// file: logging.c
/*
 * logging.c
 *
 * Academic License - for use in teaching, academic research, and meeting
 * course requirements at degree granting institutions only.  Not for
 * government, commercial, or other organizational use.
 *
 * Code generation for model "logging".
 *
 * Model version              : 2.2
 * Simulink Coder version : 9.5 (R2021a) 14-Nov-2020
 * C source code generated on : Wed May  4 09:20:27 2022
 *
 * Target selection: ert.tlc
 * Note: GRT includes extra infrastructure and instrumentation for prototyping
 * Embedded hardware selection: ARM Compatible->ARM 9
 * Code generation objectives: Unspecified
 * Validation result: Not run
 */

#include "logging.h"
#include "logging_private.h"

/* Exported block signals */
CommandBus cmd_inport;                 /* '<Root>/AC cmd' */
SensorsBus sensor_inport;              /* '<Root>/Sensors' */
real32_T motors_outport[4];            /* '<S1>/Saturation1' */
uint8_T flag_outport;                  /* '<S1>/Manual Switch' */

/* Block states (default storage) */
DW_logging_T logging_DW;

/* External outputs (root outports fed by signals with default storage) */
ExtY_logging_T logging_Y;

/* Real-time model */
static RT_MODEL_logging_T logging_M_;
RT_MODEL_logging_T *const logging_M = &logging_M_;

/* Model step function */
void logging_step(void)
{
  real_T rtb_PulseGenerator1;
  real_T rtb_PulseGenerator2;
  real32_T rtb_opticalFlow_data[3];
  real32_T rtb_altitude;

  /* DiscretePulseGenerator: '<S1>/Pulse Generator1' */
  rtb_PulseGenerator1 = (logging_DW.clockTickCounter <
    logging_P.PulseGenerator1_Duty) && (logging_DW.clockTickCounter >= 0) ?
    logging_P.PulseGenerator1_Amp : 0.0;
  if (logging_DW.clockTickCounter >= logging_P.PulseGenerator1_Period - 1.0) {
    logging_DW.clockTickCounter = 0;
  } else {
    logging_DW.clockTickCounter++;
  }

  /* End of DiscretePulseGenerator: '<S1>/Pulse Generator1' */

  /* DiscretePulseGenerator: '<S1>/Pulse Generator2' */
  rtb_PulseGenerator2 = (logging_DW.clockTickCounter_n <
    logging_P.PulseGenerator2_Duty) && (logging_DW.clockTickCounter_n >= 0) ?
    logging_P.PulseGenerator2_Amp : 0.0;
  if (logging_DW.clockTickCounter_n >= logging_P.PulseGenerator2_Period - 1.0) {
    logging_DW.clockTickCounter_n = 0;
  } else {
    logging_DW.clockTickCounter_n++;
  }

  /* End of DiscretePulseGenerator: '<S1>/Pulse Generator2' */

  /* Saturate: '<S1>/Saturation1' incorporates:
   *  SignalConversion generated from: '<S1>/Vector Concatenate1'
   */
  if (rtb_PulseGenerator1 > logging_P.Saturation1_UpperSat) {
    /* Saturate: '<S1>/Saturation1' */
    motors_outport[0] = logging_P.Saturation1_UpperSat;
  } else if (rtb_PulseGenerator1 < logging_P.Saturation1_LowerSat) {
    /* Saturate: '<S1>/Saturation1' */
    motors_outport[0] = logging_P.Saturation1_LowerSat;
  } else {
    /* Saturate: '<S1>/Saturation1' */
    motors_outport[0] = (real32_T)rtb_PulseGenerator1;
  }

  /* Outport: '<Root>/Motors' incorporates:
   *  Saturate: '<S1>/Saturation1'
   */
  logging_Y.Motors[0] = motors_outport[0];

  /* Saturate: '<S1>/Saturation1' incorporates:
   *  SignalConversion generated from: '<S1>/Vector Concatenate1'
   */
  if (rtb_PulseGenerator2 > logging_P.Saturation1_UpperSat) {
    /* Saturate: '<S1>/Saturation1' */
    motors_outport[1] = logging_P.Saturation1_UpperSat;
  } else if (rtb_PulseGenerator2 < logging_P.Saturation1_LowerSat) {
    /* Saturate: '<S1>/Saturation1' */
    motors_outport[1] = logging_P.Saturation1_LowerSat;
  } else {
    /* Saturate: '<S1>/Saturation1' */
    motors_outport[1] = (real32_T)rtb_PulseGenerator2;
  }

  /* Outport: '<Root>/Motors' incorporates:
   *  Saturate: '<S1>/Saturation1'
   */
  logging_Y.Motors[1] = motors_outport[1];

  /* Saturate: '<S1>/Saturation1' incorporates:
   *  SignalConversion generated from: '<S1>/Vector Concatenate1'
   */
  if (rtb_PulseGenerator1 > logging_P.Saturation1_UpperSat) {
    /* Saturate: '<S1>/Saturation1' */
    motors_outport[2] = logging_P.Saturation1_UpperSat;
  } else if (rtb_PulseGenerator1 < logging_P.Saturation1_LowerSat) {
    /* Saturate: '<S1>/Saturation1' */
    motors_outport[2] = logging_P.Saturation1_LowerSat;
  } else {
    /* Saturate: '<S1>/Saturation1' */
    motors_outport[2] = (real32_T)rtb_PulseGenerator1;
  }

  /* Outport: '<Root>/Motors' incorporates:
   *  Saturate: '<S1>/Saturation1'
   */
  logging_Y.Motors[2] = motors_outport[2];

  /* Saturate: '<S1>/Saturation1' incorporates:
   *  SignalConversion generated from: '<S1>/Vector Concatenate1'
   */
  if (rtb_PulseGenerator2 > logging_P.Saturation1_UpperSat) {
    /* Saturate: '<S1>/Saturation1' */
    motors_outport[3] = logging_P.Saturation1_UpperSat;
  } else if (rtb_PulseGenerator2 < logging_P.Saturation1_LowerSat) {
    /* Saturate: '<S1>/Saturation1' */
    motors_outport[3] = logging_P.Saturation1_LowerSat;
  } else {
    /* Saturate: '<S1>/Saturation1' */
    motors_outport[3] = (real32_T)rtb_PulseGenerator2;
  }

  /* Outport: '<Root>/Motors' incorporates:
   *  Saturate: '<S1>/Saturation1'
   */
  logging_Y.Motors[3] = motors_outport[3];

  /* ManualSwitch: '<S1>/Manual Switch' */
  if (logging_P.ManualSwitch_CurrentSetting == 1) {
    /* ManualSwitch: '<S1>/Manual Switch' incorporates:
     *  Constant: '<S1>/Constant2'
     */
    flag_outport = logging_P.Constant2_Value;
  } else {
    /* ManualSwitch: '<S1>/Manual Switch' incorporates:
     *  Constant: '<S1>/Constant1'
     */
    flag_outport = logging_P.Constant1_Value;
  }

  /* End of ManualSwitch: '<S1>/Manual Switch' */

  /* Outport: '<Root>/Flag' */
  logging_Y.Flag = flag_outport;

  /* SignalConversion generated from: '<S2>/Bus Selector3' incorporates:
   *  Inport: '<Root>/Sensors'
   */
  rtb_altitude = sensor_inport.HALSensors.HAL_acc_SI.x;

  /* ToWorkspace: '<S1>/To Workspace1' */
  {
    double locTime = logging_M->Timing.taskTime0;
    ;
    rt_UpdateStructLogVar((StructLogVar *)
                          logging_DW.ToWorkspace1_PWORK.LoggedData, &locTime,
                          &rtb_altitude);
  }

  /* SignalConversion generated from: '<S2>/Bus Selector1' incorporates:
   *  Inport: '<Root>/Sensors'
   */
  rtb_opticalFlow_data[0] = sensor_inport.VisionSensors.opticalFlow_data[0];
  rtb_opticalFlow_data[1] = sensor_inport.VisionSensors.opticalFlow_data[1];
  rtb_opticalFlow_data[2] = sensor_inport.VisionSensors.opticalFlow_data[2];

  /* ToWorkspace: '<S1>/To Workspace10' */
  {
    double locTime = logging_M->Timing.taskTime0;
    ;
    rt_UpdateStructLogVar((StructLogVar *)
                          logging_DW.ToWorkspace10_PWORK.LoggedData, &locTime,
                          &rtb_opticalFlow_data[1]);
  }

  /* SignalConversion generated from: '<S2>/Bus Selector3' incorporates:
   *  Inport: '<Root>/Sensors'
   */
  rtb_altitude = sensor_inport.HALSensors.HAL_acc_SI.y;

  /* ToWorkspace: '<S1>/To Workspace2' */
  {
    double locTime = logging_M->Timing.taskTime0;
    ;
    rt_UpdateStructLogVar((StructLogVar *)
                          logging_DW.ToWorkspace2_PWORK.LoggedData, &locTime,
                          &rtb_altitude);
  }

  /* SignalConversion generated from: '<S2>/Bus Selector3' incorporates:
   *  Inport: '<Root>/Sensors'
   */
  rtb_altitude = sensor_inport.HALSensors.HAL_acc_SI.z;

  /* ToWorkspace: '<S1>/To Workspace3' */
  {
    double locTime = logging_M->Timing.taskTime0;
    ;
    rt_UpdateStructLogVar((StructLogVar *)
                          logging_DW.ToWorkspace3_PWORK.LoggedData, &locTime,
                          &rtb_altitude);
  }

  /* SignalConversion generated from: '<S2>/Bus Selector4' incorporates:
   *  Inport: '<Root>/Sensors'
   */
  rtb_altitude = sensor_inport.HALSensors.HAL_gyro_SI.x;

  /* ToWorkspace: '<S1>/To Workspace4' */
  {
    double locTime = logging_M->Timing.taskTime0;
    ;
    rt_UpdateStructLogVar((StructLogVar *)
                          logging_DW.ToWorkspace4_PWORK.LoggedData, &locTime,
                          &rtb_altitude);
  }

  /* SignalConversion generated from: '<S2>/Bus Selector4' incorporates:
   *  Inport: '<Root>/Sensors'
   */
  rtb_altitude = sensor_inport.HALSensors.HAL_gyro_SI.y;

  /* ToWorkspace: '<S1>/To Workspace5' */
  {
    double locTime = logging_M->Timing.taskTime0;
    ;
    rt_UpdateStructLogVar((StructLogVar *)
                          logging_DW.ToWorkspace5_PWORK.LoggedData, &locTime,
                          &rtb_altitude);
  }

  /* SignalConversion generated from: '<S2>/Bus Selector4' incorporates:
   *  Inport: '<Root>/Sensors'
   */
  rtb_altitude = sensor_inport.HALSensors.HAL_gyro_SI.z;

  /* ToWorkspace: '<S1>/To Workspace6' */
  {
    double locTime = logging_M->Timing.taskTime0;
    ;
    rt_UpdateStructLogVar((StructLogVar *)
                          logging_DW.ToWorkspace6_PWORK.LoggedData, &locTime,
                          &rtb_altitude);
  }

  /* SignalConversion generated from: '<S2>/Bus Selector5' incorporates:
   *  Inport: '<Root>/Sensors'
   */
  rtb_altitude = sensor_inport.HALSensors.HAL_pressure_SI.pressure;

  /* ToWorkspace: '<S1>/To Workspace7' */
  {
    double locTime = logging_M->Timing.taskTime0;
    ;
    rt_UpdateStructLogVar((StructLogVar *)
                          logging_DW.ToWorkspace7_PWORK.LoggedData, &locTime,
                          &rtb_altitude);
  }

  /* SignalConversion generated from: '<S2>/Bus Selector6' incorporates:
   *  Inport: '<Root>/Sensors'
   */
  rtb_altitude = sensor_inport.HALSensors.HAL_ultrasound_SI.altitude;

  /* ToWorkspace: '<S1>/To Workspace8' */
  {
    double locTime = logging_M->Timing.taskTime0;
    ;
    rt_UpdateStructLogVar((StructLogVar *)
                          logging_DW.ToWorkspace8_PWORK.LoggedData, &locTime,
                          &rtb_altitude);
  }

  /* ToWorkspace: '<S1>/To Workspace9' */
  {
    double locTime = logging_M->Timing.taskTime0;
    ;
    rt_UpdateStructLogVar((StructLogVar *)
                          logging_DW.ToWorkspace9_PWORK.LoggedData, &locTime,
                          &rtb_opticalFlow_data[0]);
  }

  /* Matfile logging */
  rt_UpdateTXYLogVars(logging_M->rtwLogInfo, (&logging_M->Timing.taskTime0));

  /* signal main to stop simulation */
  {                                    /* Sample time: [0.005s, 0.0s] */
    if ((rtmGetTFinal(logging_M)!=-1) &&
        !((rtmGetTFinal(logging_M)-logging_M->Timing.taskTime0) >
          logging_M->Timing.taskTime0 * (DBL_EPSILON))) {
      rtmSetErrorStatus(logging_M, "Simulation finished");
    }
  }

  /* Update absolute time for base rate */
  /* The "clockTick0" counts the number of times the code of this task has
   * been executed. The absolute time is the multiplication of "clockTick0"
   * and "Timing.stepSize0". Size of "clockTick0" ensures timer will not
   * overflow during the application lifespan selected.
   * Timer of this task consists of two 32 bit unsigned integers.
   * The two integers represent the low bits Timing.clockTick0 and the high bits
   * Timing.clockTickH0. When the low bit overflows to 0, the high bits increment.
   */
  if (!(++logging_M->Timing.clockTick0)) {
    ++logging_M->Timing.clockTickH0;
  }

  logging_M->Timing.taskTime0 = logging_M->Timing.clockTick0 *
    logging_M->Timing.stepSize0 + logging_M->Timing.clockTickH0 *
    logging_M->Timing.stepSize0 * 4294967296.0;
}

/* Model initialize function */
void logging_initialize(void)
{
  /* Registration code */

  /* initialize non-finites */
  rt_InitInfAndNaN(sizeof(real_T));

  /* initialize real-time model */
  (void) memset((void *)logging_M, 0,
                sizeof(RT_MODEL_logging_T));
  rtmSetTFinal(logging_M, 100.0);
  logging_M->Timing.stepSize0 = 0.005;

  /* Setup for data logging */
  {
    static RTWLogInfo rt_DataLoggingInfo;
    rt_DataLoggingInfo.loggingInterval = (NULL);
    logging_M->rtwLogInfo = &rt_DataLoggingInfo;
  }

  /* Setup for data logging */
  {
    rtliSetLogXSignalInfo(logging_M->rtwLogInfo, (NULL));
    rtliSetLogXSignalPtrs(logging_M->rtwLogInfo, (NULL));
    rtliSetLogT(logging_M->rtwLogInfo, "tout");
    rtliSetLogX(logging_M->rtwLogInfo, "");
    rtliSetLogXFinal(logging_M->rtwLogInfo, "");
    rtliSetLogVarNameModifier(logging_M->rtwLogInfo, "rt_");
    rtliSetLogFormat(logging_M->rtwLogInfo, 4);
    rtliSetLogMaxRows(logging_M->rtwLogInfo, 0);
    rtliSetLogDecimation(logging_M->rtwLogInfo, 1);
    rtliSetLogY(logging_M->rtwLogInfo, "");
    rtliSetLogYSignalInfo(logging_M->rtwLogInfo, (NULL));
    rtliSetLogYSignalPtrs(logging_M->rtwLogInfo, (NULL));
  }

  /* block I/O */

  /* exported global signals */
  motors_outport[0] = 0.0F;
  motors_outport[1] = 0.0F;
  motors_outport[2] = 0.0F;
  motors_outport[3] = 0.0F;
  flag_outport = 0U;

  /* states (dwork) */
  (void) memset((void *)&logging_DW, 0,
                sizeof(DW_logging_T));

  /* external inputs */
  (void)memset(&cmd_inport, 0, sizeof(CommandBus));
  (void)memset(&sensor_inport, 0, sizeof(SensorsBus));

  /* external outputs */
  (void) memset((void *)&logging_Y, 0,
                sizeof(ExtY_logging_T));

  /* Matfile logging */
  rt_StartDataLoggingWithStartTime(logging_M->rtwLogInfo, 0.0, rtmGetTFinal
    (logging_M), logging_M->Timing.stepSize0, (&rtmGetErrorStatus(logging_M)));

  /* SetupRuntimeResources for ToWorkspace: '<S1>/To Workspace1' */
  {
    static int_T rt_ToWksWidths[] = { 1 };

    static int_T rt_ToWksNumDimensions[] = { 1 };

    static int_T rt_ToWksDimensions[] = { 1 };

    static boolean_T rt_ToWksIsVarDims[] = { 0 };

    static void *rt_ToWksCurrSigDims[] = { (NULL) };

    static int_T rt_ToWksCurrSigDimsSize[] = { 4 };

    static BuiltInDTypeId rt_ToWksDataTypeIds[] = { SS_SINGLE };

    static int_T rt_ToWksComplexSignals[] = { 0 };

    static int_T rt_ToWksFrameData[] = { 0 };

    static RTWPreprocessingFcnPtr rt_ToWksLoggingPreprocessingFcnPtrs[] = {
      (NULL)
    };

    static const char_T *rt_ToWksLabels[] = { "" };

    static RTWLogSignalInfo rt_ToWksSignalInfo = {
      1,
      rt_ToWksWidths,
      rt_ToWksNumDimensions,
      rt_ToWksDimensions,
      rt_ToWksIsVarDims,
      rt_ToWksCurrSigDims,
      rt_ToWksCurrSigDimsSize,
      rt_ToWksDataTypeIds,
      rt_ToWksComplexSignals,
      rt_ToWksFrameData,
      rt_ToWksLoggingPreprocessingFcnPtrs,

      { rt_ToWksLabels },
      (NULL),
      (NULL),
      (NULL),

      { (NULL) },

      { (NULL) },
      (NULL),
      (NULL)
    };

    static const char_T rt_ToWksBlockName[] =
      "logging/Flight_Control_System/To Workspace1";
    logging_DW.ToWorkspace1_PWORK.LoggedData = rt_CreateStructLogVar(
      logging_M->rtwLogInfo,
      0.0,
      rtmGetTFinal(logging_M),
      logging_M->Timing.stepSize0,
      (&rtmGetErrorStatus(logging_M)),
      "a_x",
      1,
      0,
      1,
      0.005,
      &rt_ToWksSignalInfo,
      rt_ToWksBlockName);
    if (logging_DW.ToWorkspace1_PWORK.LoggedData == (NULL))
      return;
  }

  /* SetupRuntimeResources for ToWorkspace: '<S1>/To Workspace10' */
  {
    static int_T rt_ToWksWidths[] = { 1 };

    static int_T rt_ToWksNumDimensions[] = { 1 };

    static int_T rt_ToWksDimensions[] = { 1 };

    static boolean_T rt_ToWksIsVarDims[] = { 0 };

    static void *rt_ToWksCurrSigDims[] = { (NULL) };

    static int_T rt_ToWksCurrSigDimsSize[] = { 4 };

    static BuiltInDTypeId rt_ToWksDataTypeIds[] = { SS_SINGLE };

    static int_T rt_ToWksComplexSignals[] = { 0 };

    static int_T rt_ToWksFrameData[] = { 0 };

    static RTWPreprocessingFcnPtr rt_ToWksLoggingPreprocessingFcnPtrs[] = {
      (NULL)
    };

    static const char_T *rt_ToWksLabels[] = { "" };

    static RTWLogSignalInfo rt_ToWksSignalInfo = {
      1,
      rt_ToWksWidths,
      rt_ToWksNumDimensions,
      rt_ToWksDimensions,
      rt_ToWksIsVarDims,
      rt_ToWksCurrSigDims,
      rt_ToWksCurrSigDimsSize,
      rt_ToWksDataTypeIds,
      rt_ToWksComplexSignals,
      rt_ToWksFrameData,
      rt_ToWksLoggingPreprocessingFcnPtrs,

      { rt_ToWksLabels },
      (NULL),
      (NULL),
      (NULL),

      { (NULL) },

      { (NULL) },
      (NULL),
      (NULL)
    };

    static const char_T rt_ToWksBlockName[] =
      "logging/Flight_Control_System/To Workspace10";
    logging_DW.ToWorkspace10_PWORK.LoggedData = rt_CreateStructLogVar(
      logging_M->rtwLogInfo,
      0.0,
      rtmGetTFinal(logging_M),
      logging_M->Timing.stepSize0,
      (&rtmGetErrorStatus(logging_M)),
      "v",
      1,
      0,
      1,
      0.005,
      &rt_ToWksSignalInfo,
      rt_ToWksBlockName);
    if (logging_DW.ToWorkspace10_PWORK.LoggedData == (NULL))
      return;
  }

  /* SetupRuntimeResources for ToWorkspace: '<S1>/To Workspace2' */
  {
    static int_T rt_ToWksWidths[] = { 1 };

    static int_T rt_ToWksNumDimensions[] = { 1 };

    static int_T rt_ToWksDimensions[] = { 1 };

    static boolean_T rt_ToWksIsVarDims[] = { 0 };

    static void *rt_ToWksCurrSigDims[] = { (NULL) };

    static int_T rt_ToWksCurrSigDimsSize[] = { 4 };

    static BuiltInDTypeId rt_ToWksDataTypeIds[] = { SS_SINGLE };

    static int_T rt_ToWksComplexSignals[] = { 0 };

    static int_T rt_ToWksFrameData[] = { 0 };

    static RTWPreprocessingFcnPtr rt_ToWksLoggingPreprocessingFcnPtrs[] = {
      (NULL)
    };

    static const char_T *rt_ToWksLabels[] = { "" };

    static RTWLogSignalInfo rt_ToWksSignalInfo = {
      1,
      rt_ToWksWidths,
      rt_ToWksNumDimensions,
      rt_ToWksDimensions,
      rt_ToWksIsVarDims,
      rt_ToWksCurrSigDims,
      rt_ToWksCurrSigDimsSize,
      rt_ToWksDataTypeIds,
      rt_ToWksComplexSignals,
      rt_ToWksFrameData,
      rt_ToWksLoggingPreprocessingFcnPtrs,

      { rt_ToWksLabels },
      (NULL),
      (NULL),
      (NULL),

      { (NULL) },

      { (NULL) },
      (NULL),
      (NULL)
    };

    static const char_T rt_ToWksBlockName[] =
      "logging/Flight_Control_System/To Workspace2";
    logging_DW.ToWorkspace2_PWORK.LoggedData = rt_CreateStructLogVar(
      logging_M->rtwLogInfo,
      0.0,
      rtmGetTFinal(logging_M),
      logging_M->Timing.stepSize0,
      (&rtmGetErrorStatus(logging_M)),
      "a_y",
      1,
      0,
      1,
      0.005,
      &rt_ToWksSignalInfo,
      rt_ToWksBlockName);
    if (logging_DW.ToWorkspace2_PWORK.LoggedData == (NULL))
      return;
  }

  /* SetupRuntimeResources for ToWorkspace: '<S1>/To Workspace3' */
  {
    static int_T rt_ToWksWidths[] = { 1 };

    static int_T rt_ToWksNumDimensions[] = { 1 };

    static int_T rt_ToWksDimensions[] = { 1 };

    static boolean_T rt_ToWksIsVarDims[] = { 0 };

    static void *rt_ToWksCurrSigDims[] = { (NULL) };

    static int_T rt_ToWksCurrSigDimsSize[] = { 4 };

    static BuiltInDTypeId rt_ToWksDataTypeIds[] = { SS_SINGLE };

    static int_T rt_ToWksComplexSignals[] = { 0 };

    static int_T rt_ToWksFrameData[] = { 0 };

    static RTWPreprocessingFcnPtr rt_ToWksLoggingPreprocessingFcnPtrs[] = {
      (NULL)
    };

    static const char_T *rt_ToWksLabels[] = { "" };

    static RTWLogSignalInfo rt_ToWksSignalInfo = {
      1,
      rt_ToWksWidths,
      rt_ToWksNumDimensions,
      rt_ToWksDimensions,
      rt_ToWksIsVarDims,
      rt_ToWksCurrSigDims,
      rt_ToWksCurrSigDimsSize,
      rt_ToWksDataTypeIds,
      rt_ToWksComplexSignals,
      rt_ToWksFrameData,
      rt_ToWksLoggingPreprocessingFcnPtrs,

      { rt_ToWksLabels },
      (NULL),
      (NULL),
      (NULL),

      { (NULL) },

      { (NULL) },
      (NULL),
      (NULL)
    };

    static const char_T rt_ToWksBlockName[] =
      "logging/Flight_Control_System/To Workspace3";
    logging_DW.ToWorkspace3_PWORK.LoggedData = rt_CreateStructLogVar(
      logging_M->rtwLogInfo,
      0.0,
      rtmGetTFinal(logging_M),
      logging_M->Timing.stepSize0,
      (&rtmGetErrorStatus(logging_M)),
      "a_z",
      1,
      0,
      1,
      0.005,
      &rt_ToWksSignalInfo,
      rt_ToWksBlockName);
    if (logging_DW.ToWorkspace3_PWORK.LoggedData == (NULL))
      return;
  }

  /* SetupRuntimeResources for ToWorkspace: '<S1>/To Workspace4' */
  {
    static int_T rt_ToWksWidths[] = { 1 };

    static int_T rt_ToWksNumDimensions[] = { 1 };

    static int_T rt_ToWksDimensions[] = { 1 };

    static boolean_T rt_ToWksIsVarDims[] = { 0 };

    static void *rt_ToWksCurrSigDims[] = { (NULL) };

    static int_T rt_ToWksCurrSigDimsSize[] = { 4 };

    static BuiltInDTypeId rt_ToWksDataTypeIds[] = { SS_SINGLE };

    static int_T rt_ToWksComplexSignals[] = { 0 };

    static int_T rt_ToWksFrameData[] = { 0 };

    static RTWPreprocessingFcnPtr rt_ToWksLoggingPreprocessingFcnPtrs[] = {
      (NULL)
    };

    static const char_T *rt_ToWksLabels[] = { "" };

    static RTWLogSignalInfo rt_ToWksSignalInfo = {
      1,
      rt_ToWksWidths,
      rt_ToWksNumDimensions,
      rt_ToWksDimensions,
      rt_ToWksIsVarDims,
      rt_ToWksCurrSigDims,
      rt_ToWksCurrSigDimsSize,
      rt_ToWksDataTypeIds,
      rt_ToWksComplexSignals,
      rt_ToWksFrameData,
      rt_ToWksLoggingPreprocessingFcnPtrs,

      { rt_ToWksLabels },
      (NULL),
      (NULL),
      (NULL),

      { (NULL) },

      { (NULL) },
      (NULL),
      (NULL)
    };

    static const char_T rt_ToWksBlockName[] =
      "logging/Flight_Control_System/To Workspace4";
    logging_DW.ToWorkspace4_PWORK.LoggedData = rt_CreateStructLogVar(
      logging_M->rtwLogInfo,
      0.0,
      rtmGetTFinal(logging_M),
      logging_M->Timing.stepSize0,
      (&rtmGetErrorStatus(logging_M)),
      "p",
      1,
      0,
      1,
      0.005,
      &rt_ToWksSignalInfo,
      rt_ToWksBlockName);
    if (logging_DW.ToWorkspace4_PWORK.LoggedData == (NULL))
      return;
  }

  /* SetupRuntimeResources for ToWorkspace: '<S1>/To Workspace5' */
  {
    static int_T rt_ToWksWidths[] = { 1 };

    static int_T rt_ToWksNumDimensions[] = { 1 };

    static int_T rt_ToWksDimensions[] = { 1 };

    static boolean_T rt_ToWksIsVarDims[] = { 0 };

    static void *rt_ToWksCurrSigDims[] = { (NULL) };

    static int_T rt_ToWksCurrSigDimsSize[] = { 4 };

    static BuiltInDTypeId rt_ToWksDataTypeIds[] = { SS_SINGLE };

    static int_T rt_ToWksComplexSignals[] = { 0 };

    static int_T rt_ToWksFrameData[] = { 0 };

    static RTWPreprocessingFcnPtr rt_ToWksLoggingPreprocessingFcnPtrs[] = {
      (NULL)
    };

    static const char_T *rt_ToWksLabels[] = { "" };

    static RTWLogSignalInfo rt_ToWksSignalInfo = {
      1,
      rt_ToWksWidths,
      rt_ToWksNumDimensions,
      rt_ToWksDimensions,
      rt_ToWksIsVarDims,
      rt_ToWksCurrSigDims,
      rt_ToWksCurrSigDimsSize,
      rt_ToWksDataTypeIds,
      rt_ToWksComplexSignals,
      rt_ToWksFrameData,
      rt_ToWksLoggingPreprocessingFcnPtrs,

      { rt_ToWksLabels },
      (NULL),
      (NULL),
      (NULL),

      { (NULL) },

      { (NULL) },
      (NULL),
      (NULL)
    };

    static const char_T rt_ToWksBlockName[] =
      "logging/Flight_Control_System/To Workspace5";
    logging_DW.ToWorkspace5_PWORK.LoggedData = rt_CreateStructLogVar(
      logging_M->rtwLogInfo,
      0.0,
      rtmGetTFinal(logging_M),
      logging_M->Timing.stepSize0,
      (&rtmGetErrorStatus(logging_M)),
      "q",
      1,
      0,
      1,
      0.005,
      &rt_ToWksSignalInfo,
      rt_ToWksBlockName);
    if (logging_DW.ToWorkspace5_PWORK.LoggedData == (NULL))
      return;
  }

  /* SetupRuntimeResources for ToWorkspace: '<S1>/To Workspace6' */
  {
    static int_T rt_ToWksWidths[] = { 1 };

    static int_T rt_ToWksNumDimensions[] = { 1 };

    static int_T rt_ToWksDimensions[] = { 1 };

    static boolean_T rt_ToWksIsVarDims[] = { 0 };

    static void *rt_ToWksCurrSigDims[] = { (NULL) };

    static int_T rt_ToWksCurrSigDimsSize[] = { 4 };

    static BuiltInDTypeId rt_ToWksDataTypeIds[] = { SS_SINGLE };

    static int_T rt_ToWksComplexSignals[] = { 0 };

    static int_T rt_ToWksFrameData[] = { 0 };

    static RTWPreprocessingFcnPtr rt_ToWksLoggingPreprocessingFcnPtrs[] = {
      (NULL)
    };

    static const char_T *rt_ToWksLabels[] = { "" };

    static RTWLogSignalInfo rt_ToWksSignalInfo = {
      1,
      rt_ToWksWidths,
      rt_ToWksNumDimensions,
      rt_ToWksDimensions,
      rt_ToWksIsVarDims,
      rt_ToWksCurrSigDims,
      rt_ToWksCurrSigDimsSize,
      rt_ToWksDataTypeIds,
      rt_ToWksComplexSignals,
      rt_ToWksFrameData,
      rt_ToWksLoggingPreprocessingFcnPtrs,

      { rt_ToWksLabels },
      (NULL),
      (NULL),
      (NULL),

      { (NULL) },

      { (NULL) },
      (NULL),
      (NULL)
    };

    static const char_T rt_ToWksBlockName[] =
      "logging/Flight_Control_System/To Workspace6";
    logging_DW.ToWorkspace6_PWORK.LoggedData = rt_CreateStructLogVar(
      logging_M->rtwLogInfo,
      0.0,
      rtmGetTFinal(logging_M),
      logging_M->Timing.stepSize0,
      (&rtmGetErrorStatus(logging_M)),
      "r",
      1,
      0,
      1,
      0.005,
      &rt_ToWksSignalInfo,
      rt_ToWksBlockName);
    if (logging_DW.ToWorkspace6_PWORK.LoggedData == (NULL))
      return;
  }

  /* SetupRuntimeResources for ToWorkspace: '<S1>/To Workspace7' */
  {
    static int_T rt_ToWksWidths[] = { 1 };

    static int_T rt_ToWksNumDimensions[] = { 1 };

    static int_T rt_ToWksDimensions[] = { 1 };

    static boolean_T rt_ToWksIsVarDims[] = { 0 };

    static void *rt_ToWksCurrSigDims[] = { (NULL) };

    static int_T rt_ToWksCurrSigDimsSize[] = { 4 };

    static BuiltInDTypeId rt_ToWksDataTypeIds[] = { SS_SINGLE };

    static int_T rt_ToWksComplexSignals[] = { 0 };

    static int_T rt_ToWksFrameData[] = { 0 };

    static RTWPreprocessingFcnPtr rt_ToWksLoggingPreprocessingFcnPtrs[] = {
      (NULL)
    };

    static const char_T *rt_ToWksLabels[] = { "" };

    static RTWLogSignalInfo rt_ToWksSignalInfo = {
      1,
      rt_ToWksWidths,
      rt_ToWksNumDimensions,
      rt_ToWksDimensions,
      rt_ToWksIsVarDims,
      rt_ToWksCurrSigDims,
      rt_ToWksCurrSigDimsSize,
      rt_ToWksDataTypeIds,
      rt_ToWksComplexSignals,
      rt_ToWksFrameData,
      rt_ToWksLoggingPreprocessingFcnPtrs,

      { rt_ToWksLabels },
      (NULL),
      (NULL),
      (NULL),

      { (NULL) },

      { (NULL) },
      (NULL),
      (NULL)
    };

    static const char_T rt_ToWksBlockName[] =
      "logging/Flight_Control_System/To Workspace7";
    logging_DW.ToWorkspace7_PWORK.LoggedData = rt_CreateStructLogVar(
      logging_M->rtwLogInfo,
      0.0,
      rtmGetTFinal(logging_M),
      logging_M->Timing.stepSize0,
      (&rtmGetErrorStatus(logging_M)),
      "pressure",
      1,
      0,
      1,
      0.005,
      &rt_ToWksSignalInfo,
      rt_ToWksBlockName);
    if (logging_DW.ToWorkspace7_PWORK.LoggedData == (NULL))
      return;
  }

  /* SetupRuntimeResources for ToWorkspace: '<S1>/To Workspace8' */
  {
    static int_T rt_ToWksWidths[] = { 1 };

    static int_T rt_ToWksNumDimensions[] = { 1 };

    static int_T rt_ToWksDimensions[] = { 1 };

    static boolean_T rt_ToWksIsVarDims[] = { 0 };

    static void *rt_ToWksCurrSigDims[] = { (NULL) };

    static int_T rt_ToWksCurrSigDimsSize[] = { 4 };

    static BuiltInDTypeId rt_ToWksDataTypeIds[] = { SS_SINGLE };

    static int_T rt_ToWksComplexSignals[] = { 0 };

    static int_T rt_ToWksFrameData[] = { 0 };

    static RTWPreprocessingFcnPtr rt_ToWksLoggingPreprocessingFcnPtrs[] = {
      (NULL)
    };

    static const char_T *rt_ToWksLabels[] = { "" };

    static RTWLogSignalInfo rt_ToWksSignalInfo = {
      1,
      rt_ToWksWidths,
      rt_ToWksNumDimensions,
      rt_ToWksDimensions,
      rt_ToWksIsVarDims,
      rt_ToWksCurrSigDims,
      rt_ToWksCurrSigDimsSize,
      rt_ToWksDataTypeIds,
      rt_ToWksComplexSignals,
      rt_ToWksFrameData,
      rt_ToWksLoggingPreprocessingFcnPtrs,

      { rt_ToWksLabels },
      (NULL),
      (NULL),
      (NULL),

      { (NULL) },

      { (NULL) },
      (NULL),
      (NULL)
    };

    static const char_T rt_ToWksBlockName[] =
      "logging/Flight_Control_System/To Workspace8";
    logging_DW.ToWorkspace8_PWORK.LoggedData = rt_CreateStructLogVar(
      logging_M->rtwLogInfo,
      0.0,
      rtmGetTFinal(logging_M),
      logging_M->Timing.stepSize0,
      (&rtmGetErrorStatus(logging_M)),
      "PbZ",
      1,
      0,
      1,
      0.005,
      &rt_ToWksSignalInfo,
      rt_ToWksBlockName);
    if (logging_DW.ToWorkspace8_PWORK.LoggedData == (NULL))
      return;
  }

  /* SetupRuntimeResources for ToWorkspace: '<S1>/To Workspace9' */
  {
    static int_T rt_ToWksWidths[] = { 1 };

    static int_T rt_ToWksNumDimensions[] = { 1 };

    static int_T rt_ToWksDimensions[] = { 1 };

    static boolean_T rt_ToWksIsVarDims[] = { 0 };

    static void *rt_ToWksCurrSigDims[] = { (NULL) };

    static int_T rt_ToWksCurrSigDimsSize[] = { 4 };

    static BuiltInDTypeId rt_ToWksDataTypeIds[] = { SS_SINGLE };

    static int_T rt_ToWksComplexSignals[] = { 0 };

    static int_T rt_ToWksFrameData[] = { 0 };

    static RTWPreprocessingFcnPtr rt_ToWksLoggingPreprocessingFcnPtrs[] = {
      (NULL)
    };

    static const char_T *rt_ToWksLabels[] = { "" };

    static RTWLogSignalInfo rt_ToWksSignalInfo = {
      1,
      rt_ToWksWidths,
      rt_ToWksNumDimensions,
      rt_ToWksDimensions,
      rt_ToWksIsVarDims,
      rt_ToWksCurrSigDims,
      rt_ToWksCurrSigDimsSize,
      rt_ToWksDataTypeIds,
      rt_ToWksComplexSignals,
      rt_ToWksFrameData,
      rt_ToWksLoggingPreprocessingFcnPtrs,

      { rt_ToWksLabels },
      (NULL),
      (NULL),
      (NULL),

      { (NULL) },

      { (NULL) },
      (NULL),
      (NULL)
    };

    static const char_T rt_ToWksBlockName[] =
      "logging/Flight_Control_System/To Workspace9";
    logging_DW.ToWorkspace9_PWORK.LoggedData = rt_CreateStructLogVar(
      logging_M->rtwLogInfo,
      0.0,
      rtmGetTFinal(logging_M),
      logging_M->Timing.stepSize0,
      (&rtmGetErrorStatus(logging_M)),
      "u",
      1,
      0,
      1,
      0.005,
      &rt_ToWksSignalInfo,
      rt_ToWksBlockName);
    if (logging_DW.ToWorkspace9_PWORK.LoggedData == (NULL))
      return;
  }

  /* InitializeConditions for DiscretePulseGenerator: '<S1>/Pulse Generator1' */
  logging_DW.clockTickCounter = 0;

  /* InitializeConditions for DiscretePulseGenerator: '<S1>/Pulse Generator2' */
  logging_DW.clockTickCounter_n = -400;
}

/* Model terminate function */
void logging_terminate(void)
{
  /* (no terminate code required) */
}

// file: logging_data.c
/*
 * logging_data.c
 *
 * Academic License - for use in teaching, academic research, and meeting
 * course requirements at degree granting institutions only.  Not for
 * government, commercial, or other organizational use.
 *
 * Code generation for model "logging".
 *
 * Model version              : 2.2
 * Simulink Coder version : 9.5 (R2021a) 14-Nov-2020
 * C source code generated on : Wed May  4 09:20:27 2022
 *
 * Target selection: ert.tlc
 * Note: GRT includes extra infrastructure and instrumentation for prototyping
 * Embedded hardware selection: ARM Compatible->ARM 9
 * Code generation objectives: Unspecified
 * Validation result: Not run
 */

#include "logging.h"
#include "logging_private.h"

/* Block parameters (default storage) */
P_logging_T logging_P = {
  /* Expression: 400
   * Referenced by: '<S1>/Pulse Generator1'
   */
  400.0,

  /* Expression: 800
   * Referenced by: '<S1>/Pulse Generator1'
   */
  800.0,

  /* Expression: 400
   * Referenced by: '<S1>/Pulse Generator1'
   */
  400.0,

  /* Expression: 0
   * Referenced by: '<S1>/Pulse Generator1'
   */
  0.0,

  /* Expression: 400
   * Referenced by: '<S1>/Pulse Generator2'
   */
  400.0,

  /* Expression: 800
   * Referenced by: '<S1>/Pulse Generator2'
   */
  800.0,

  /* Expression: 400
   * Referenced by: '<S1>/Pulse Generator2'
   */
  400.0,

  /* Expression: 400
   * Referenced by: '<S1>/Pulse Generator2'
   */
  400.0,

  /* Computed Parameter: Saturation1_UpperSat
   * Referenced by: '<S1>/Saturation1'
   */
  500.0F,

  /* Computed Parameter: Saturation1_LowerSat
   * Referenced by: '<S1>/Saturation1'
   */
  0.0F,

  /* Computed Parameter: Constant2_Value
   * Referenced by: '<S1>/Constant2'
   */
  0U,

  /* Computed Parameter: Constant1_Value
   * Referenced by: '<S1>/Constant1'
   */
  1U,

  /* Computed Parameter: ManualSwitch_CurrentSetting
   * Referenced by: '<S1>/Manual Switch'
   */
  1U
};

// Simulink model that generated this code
simulink model "logging"  (R2021a)
settings: Solver=FixedStepAuto  StartTime=0.0  StopTime=100  RelTol=1e-3
InitFcn:
  | load('BusDefinitions.mat')
undefined symbols (not defined in the file or in its folder): codertarget, Ts

== system logging ==
  note: Model your control logic inside this subsystem using the Sensor
      | values and output the Motor values
  note: DO NOT MODIFY these output ports and
      | signal properties.
      |
      | Always ensure the 'Motors' outport is fed
      | with a 1 X 4 single vector.
      |
      |
      |
      |
      | Always ensure the 'Flag' outport is fed
      | with a 1 X 1 uint8 value.
  note: DO NOT MODIFY these input ports and
      | signal properties.
  note: This model spins the motors 1 and 3 for 2s, then spins motors 2 and 4 for 2s and so on.
  note: Copyright 2017-2020 The MathWorks, Inc.
  note: Parrot Getting Started
  AC cmd : Inport  OutDataTypeStr=Bus: CommandBus  BusOutputAsStruct=on
  Sensors : Inport  Port=2  OutDataTypeStr=Bus: SensorsBus  BusOutputAsStruct=on
  Flight_Control_System : Subsystem  InitFcn=codertarget.parrot.internal.fcsSubsystemCallback(gcb);
  Motors : Outport  OutDataTypeStr=single  PortDimensions=[1 4]  VectorParamsAs1DForOutWhenUnconnected=off
  Flag : Outport  Port=2  OutDataTypeStr=uint8  PortDimensions=1  VectorParamsAs1DForOutWhenUnconnected=off
  wires:
  Flight_Control_System/1(Motors) -> Motors/1  "Motor"
  AC cmd/1 -> Flight_Control_System/1(AC cmd)  "Command"
  Sensors/1 -> Flight_Control_System/2(Sensors)  "Sensor_values"
  Flight_Control_System/2(Flag) -> Flag/1  "flag"

== system logging/Flight_Control_System ==
  note: The 'Motors' outport is fed with the speed values of the 4 motors.
  note: Model an error condition and feed the value to 'Flag' outport block.
      | Value '0' indicates that all the flight conditions are good and the drone
      | can continue its flight.
      | A non-zero value indicates an error condition, and stops the drone
      | flight.
  note: The SensorsBus contains data from sensors like
      | accelerometer, gyroscope, ultrasonic, pressure,
      | and optical flow data.
  AC cmd : Inport
  Sensors : Inport  Port=2
  Bus Selector : BusSelector  OutputSignals=controlModePosVSOrient,pos_ref,takeoff_flag,orient_ref,live_time_ticks
  Bus Selector1 : BusSelector  OutputSignals=VisionSensors,HALSensors,SensorCalibration
  Constant1 : Constant  OutDataTypeStr=uint8
  Constant2 : Constant  Value=0  OutDataTypeStr=uint8
  Demux : Demux  Outputs=3
  Manual Switch : ManualSwitch
  Pulse Generator1 : DiscretePulseGenerator  Amplitude=400  Period=800  PulseWidth=400  SampleTime=Ts
  Pulse Generator2 : DiscretePulseGenerator  Amplitude=400  Period=800  PulseWidth=400  PhaseDelay=400  SampleTime=Ts
  Saturation1 : Saturate  UpperLimit=500  LowerLimit=0  OutDataTypeStr=single
  Subsystem : Subsystem
  Terminator{,1,3..7,17..18} (9 alike) : Terminator
  To Workspace1 : ToWorkspace  VariableName=a_x  SaveFormat=Structure With Time  SampleTime=-1
  To Workspace10 : ToWorkspace  VariableName=v  SaveFormat=Structure With Time  SampleTime=-1
  To Workspace2 : ToWorkspace  VariableName=a_y  SaveFormat=Structure With Time  SampleTime=-1
  To Workspace3 : ToWorkspace  VariableName=a_z  SaveFormat=Structure With Time  SampleTime=-1
  To Workspace4 : ToWorkspace  VariableName=p  SaveFormat=Structure With Time  SampleTime=-1
  To Workspace5 : ToWorkspace  VariableName=q  SaveFormat=Structure With Time  SampleTime=-1
  To Workspace6 : ToWorkspace  VariableName=r  SaveFormat=Structure With Time  SampleTime=-1
  To Workspace7 : ToWorkspace  VariableName=pressure  SaveFormat=Structure With Time  SampleTime=-1
  To Workspace8 : ToWorkspace  VariableName=PbZ  SaveFormat=Structure With Time  SampleTime=-1
  To Workspace9 : ToWorkspace  VariableName=u  SaveFormat=Structure With Time  SampleTime=-1
  Vector Concatenate1 : Concatenate  NumInputs=4
  Motors : Outport  VectorParamsAs1DForOutWhenUnconnected=off
  Flag : Outport  Port=2  VectorParamsAs1DForOutWhenUnconnected=off
  wires:
  AC cmd/1 -> Bus Selector/1
  Bus Selector/1 -> Terminator3/1  "<controlModePosVSOrient>"
  Bus Selector/2 -> Terminator4/1  "<pos_ref>"
  Bus Selector/3 -> Terminator5/1  "<takeoff_flag>"
  Bus Selector/4 -> Terminator6/1  "<orient_ref>"
  Bus Selector/5 -> Terminator7/1  "<live_time_ticks>"
  Manual Switch/1 -> Flag/1
  Constant2/1 -> Manual Switch/1
  Constant1/1 -> Manual Switch/2
  Saturation1/1 -> Motors/1
  Vector Concatenate1/1 -> Saturation1/1
  Pulse Generator1/1 -> Vector Concatenate1/3, Vector Concatenate1/1
  Pulse Generator2/1 -> Vector Concatenate1/2, Vector Concatenate1/4
  Subsystem/6(q) -> To Workspace5/1
  Subsystem/11(vbat_percentage) -> Terminator18/1
  Bus Selector1/3 -> Terminator/1  "<SensorCalibration>"
  Subsystem/8(prs) -> To Workspace7/1
  Bus Selector1/2 -> Subsystem/2(<HALSensors>)  "<HALSensors>"
  Bus Selector1/1 -> Subsystem/1(<VisionSensors>)  "<VisionSensors>"
  Subsystem/7(r) -> To Workspace6/1
  Subsystem/1(OF_data) -> Demux/1
  Subsystem/4(ddz) -> To Workspace3/1
  Subsystem/3(ddy) -> To Workspace2/1
  Subsystem/9(altitude_sonar) -> To Workspace8/1
  Subsystem/10(vbat_V) -> Terminator17/1
  Subsystem/2(ddx) -> To Workspace1/1
  Subsystem/5(p) -> To Workspace4/1
  Sensors/1 -> Bus Selector1/1
  Demux/3 -> Terminator1/1
  Demux/1 -> To Workspace9/1
  Demux/2 -> To Workspace10/1

== system logging/Flight_Control_System/Subsystem ==
  <VisionSensors> : Inport
  <HALSensors> : Inport  Port=2
  Bus Selector1 : BusSelector  OutputSignals=opticalFlow_data
  Bus Selector2 : BusSelector  OutputSignals=HAL_acc_SI,HAL_gyro_SI,HAL_pressure_SI,HAL_ultrasound_SI,HAL_vbat_SI
  Bus Selector3 : BusSelector  OutputSignals=x,y,z
  Bus Selector4 : BusSelector  OutputSignals=x,y,z
  Bus Selector5 : BusSelector  OutputSignals=pressure
  Bus Selector6 : BusSelector  OutputSignals=altitude
  Bus Selector7 : BusSelector  OutputSignals=vbat_V,vbat_percentage
  OF_data : Outport  VectorParamsAs1DForOutWhenUnconnected=off
  ddx : Outport  Port=2  VectorParamsAs1DForOutWhenUnconnected=off
  ddy : Outport  Port=3  VectorParamsAs1DForOutWhenUnconnected=off
  ddz : Outport  Port=4  VectorParamsAs1DForOutWhenUnconnected=off
  p : Outport  Port=5  VectorParamsAs1DForOutWhenUnconnected=off
  q : Outport  Port=6  VectorParamsAs1DForOutWhenUnconnected=off
  r : Outport  Port=7  VectorParamsAs1DForOutWhenUnconnected=off
  prs : Outport  Port=8  VectorParamsAs1DForOutWhenUnconnected=off
  altitude_sonar : Outport  Port=9  VectorParamsAs1DForOutWhenUnconnected=off
  vbat_V : Outport  Port=10  VectorParamsAs1DForOutWhenUnconnected=off
  vbat_percentage : Outport  Port=11  VectorParamsAs1DForOutWhenUnconnected=off
  wires:
  <VisionSensors>/1 -> Bus Selector1/1
  <HALSensors>/1 -> Bus Selector2/1
  Bus Selector1/1 -> OF_data/1  "<opticalFlow_data>"
  Bus Selector2/1 -> Bus Selector3/1  "<HAL_acc_SI>"
  Bus Selector2/2 -> Bus Selector4/1  "<HAL_gyro_SI>"
  Bus Selector2/3 -> Bus Selector5/1  "<HAL_pressure_SI>"
  Bus Selector2/4 -> Bus Selector6/1  "<HAL_ultrasound_SI>"
  Bus Selector2/5 -> Bus Selector7/1  "<HAL_vbat_SI>"
  Bus Selector3/1 -> ddx/1  "<x>"
  Bus Selector3/2 -> ddy/1  "<y>"
  Bus Selector3/3 -> ddz/1  "<z>"
  Bus Selector4/2 -> q/1  "<y>"
  Bus Selector4/1 -> p/1  "<x>"
  Bus Selector4/3 -> r/1  "<z>"
  Bus Selector5/1 -> prs/1  "<pressure>"
  Bus Selector6/1 -> altitude_sonar/1  "<altitude>"
  Bus Selector7/1 -> vbat_V/1  "<vbat_V>"
  Bus Selector7/2 -> vbat_percentage/1  "<vbat_percentage>"
